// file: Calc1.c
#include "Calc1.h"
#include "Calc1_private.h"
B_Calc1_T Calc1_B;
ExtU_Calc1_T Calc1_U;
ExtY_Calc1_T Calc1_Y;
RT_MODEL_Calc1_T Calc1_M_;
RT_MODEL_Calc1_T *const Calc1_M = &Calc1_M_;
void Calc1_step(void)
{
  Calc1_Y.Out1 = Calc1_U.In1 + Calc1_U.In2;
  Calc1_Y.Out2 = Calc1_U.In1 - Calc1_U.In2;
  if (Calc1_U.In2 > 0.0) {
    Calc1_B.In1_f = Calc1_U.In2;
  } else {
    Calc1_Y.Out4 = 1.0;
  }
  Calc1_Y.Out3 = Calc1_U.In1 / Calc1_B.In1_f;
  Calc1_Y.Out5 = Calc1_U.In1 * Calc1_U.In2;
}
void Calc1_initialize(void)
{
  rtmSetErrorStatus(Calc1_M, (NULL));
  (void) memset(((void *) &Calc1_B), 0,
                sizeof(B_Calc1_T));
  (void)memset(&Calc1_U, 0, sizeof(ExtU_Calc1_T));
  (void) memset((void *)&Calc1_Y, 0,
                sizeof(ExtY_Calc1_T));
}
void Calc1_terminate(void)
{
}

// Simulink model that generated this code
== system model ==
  In1 : Inport
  In2 : Inport
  Out1 : Outport  <- 1: Sum#1
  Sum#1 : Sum  <- 1: In1, 2: In2
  Out2 : Outport  <- 1: Sum#2
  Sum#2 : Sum  Inputs=+-  <- 1: In1, 2: In2
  Out3 : Outport  <- 1: Product#1
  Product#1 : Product  Inputs=*/  <- 1: In1, 2: Subsystem#1
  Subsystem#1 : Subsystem  <- 1: In2, Action: If#1
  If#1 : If  <- 1: In2
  Out4 : Outport  <- 1: Subsystem#2
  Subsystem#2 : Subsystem  <- 1: Constant#1, Action: If#1/2
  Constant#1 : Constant
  Out5 : Outport  <- 1: Product#2
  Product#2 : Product  <- 1: In1, 2: In2
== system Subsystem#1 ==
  Inport#1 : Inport
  ActionPort#1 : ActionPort
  Outport#1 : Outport  <- 1: Inport#1
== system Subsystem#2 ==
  Inport#2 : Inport
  ActionPort#2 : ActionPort
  Outport#2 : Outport  <- 1: Inport#2
